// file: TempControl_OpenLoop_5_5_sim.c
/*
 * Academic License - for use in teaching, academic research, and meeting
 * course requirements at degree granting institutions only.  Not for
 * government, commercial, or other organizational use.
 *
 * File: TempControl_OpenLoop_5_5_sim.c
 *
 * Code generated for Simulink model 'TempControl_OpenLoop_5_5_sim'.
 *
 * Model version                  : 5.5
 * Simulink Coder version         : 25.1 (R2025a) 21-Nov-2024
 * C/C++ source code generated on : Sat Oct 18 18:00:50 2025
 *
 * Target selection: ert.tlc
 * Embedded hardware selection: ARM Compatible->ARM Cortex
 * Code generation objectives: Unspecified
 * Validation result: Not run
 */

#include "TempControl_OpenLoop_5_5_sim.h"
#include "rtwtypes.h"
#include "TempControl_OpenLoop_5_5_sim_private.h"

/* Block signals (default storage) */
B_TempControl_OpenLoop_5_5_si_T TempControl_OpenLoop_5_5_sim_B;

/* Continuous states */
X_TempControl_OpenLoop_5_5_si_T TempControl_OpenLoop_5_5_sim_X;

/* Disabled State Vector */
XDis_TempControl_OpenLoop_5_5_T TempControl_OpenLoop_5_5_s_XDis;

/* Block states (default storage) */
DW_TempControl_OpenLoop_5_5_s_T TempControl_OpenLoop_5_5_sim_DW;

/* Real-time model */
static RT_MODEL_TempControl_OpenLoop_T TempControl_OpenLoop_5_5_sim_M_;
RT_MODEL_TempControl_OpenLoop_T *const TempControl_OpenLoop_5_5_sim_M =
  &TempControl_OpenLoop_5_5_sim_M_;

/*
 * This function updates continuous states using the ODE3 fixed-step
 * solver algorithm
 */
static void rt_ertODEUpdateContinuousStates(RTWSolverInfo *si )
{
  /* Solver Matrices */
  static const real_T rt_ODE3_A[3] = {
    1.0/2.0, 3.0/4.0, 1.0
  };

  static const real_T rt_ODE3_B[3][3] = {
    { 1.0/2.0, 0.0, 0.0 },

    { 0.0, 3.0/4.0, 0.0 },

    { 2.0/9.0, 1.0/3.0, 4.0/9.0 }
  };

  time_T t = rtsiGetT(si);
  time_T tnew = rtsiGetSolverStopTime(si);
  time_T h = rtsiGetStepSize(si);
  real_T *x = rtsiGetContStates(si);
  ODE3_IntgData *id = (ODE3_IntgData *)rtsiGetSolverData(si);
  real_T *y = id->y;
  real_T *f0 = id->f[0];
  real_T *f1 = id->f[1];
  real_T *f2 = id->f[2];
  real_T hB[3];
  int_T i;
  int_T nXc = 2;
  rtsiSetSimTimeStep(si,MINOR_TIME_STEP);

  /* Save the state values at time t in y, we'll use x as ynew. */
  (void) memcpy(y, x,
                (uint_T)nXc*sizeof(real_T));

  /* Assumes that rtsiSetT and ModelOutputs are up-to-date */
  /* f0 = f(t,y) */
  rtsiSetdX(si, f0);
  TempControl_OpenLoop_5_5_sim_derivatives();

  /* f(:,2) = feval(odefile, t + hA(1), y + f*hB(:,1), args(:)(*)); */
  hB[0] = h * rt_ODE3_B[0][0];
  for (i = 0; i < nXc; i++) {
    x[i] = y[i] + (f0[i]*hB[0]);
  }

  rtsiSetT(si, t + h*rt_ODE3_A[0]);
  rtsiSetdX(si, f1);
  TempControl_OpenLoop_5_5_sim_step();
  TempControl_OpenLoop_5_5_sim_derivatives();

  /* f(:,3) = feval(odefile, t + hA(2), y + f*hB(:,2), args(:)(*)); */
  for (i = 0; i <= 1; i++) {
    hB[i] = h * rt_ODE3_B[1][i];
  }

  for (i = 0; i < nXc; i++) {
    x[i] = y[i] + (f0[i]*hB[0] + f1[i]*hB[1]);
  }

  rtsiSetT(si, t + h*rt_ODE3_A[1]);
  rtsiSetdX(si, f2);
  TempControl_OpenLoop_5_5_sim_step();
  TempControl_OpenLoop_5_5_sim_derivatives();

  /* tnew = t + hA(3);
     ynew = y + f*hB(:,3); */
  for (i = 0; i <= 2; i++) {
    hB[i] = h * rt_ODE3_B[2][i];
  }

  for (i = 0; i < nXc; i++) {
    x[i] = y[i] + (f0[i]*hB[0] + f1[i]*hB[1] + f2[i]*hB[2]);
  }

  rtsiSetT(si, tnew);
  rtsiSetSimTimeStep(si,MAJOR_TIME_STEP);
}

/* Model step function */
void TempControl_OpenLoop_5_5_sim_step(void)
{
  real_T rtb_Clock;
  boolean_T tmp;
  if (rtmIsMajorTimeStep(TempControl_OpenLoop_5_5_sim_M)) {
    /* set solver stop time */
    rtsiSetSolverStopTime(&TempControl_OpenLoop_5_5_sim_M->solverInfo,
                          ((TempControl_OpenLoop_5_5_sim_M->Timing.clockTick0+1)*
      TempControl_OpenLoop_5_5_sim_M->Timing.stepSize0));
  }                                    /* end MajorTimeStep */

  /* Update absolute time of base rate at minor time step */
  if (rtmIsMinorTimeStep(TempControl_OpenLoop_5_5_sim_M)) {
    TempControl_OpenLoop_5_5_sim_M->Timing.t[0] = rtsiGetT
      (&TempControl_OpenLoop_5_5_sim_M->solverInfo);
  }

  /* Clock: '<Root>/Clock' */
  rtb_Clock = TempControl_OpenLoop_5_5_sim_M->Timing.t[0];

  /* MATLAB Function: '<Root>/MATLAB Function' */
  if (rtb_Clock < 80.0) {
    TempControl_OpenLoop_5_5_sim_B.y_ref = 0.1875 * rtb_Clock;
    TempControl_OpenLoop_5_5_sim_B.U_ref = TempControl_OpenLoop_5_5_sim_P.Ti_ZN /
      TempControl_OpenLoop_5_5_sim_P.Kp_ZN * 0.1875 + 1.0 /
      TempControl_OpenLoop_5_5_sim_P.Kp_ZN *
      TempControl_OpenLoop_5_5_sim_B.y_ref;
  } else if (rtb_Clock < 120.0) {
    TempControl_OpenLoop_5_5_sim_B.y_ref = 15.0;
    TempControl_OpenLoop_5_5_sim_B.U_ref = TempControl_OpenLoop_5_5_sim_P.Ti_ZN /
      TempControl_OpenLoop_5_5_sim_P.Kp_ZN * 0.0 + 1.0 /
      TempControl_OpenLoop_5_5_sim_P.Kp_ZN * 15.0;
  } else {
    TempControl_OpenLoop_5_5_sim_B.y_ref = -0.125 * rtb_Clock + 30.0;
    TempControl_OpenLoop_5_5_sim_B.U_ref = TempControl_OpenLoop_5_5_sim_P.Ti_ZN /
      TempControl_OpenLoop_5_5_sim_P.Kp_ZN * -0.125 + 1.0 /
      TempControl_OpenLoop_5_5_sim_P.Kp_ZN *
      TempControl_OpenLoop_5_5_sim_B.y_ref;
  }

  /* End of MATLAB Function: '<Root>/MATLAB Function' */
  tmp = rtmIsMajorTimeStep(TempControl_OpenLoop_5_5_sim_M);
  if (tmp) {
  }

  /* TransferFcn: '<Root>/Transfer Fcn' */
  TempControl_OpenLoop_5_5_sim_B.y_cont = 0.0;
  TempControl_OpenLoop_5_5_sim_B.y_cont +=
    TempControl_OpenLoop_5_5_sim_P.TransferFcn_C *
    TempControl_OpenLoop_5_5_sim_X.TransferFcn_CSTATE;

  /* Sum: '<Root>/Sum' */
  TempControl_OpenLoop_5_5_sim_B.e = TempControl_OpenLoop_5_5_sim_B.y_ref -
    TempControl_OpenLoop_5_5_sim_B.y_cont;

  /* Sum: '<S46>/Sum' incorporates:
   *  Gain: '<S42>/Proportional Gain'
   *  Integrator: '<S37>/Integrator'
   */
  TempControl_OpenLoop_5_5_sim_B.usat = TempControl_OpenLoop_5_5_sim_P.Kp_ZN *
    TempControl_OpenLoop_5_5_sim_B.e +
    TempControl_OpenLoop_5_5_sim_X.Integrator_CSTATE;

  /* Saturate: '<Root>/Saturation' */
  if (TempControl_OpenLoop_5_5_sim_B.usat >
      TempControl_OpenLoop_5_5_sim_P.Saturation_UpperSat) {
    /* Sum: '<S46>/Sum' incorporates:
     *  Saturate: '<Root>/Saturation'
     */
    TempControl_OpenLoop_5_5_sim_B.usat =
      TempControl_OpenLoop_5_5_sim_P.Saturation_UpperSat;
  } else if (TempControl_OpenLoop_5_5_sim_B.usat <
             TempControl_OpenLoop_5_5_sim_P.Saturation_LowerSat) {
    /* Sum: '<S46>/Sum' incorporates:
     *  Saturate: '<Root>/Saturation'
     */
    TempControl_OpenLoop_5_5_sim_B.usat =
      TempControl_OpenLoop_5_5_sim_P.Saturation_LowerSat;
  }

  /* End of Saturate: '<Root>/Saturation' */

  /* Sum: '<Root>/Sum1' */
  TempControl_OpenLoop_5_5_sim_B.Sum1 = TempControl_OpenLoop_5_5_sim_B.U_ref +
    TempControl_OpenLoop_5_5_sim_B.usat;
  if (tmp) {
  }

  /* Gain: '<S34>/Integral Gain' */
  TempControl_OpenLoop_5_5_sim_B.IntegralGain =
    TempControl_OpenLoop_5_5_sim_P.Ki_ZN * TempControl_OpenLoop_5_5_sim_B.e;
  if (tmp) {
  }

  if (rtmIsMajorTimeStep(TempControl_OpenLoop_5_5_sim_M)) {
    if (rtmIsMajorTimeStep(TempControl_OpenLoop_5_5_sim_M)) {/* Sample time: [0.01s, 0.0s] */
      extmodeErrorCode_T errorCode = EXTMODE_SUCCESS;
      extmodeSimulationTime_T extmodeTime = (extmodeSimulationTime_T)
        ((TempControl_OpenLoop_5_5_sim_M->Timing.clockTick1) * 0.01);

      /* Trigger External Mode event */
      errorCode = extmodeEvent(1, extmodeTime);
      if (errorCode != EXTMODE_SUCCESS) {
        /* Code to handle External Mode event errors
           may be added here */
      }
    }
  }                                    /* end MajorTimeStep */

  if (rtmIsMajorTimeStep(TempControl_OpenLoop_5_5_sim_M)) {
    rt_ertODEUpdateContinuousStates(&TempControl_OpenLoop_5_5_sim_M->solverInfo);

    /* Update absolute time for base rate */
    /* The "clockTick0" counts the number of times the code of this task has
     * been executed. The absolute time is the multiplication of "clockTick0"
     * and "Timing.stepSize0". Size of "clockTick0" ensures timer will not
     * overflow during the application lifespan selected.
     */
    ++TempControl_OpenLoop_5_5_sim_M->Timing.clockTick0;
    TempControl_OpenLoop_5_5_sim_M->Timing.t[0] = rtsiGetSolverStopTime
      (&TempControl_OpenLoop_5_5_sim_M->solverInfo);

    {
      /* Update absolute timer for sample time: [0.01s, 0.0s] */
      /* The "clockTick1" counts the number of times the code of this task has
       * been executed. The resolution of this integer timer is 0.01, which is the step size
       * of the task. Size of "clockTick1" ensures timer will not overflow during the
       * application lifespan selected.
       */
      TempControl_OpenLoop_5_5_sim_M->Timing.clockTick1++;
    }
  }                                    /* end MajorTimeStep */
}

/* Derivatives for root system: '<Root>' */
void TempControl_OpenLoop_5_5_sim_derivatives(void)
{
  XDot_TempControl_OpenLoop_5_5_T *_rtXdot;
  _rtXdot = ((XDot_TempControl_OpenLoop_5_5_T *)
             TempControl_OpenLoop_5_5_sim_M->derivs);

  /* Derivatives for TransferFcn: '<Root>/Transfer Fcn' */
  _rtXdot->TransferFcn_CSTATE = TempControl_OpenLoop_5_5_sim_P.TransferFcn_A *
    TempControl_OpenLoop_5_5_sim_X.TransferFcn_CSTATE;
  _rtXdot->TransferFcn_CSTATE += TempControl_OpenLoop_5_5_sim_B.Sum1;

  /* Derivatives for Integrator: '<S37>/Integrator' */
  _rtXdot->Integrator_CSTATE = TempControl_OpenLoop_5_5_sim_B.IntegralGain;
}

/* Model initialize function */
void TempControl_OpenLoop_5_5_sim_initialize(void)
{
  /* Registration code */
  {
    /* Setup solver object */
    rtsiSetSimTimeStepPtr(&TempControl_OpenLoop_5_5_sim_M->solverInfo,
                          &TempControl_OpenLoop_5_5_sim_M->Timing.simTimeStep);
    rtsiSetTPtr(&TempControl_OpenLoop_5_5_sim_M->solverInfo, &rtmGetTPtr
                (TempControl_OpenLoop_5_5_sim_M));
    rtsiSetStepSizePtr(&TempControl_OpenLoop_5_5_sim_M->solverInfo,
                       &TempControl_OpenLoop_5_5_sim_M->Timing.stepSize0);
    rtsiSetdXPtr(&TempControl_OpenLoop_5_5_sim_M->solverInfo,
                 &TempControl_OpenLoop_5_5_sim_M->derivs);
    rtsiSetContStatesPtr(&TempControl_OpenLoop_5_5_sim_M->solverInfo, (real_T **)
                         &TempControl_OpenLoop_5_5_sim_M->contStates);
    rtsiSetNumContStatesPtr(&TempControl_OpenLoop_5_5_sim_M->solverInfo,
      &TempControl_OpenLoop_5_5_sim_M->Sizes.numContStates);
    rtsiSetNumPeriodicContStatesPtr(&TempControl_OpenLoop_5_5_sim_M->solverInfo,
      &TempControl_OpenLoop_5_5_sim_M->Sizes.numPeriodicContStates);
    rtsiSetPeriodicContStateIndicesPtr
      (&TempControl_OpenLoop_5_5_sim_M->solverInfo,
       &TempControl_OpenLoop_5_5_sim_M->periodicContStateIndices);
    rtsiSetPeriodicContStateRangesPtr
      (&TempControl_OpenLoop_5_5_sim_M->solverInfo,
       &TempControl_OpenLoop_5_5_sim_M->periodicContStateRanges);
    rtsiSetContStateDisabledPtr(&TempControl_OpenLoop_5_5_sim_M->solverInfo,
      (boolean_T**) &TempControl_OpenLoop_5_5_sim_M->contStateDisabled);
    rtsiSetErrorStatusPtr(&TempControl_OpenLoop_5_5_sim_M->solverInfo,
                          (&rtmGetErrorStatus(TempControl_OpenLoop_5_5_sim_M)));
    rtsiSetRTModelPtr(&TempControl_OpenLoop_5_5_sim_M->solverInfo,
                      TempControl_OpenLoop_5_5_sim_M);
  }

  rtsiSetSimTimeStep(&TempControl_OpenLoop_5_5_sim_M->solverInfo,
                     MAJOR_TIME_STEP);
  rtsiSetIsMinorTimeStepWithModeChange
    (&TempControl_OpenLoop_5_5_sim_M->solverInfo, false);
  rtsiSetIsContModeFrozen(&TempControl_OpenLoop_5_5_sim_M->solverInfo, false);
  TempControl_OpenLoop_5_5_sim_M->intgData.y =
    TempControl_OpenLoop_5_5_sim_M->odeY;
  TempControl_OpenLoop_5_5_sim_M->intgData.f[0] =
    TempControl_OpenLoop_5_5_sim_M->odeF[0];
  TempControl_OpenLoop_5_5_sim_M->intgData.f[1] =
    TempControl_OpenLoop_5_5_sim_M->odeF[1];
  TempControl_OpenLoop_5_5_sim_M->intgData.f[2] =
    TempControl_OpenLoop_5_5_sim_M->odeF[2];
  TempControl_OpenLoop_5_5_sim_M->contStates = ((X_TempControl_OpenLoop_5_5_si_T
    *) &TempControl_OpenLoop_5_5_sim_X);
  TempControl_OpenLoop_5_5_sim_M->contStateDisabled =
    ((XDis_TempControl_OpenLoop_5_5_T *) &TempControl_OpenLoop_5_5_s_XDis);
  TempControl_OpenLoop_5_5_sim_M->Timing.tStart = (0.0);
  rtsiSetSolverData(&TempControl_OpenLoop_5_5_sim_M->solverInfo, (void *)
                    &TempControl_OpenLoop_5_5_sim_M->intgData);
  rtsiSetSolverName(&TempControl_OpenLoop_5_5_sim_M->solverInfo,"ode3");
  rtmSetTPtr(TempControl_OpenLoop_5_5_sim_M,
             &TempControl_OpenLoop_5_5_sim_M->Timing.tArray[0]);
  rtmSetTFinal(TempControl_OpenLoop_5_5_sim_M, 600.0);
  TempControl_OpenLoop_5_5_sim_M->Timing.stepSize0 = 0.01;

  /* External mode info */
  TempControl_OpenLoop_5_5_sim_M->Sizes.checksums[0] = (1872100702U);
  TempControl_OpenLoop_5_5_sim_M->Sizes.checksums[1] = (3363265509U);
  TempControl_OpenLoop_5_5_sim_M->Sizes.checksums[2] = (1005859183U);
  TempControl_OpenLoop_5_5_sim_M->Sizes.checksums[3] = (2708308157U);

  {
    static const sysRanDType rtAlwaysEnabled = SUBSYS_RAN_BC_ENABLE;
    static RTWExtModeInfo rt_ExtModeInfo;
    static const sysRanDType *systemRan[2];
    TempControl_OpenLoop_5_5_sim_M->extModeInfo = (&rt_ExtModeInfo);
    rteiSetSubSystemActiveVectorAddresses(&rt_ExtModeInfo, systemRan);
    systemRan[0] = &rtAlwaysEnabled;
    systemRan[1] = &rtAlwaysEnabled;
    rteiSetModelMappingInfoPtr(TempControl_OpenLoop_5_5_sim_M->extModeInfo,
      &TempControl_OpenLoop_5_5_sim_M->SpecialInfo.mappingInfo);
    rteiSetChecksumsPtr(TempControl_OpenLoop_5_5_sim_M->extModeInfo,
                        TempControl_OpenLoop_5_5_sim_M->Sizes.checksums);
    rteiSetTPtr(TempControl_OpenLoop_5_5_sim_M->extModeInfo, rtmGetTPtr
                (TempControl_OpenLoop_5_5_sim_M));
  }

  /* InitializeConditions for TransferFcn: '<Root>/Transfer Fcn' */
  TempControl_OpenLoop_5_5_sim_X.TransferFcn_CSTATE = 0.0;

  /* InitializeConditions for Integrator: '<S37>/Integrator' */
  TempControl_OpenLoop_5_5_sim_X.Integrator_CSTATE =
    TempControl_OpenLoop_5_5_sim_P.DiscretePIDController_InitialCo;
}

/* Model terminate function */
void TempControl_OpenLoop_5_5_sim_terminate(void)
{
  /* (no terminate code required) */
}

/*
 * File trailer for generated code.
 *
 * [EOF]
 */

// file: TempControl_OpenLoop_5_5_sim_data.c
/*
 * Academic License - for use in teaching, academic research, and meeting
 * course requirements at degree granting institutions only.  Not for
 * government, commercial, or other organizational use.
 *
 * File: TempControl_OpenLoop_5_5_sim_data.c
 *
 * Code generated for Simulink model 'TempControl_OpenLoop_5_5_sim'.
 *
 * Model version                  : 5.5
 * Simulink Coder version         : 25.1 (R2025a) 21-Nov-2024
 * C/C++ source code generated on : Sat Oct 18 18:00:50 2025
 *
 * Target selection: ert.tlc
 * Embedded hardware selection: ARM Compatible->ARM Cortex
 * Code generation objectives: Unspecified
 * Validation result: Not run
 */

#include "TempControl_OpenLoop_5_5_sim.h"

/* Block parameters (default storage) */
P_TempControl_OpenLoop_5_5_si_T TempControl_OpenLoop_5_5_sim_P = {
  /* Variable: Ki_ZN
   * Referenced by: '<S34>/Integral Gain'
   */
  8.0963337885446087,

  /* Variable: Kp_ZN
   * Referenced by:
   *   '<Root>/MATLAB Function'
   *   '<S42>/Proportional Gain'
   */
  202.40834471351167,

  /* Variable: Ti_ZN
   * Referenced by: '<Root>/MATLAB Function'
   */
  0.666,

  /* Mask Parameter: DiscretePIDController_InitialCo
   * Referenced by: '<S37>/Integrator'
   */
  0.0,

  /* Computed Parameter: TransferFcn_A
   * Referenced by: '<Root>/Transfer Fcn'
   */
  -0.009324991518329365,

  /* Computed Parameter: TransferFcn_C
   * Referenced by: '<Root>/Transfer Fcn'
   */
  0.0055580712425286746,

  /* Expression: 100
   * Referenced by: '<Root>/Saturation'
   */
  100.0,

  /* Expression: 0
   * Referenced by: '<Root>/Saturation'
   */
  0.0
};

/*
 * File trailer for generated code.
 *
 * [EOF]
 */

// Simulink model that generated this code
simulink model "TempControl_OpenLoop_5_5_sim"  (R2025a)
settings: Solver=FixedStepAuto  StartTime=0.0  StopTime=600  FixedStep=10e-3  RelTol=1e-3  EnableMultiTasking=on
undefined symbols (not defined in the file or in its folder): G_s, Ki_ZN, Kp_ZN, Ti_ZN
libraries: slpidlib x1

== system TempControl_OpenLoop_5_5_sim ==
  Clock : Clock
  Discrete PID Controller : slpidlib/PID Controller  Controller=PI  Form=Parallel  TimeDomain=Continuous-time  UseExternalTs=off  SampleTime=-1  IntegratorMethod=Forward Euler  FilterMethod=Forward Euler  ControllerParametersSource=internal  P=Kp_ZN  I=Ki_ZN  UseKiTs=off  D=0  UseExternalDerivativeSource=off  N=100  UseFilter=on  TunerSelectOption=Transfer Function Based (PID Tuner App)  InitialConditionSource=internal  InitialConditionForIntegrator=0  InitialConditionForFilter=0  DifferentiatorICPrevScaledInput=0  ExternalReset=none  TrackingMode=off  Kt=1  LimitOutput=off  SatLimitsSource=internal  UpperSaturationLimit=inf  LowerSaturationLimit=-inf  LinearizeAsGain=off  AntiWindupMode=none  Kb=1  LimitIntegrator=off  UpperIntegratorSaturationLimit=inf  LowerIntegratorSaturationLimit=-inf  POutMin=[]  POutMax=[]  IOutMin=[]  IOutMax=[]  DOutMin=[]  DOutMax=[]  NOutMin=[]  NOutMax=[]  SumOutMin=[]  SumOutMax=[]  SaturationOutMin=[]  SaturationOutMax=[]  PParamMin=[]  PParamMax=[]  IParamMin=[]  IParamMax=[]  DParamMin=[]  DParamMax=[]  NParamMin=[]  NParamMax=[]  KbParamMin=[]  KbParamMax=[]  KtParamMin=[]  KtParamMax=[]  KbOutMin=[]  KbOutMax=[]  KtOutMin=[]  KtOutMax=[]  IntegratorOutMin=[]  IntegratorOutMax=[]  FilterOutMin=[]  FilterOutMax=[]  SumI1OutMin=[]  SumI1OutMax=[]  SumI2OutMin=[]  SumI2OutMax=[]  SumI3OutMin=[]  SumI3OutMax=[]  SumI4OutMin=[]  SumI4OutMax=[]  SumDOutMin=[]  SumDOutMax=[]  DifferentiatorOutMin=[]  DifferentiatorOutMax=[]  FilterDiffOutCoefMin=[]  FilterDiffOutCoefMax=[]  ReciprocalOutMin=[]  ReciprocalOutMax=[]  SumDenOutMin=[]  SumDenOutMax=[]  SumNumOutMin=[]  SumNumOutMax=[]  DivideOutMin=[]  DivideOutMax=[]  UdiffTsProdOutMin=[]  UdiffTsProdOutMax=[]  NTsProdOutMin=[]  NTsProdOutMax=[]  UintegralTsProdOutMin=[]  UintegralTsProdOutMax=[]  UngainTsProdOutMin=[]  UngainTsProdOutMax=[]  ClampingZeroOutDataTypeStr=Inherit: Inherit via back propagation  ClampingZeroOutMin=[]  ClampingZeroOutMax=[]  FilterDenConstantOutDataTypeStr=Inherit: Inherit via back propagation  FilterDenConstantOutMin=[]  FilterDenConstantOutMax=[]  PCopyOutDataTypeStr=Inherit: Inherit via back propagation  PCopyOutMin=[]  PCopyOutMax=[]  NCopyOutDataTypeStr=Inherit: Inherit via back propagation  NCopyOutMin=[]  NCopyOutMax=[]  IntegratorContinuousStateAttributes=''  IntegratorStateMustResolveToSignalObject=off  IntegratorRTWStateStorageClass=Auto  FilterContinuousStateAttributes=''  FilterStateMustResolveToSignalObject=off  FilterRTWStateStorageClass=Auto  ParallelPVariant=InternalParameters  IdealPVariant=Disabled  IVariant=InternalParameters  DVariant=Disabled  IntegratorVariant=Continuous  SatVariant=Disabled  AWVariant=Passthrough  PCopyVariant=Disabled  TRVariant=Disabled  FdbkBlocksVariant=Forward  IdealPFdbkVariant=Disabled  SatFdbkVariant=Disabled  DerivativeFilterVariant=Disabled  NVariant=Disabled  NCopyVariant=Disabled_SignalSpec  FilterICVariant=Disabled  IntegratorICVariant=InternalICs  ExternalResetVariant=Disabled  TRSumVariant=Passthrough  SumFdbkVariant=Disabled  SumVariant=Sum_PI  TsampFilterVariant=InternalTs  TsampNgainVariant=Passthrough  TsampIntegralVariant=Disabled_SignalSpec  ExternalSaturationOutDataTypeStr=Inherit: Same as second input  DerivativeSourceVariant=Disabled  PreIntVariant=InternalPreInt
  MATLAB Function : MATLAB Function  TreatAsAtomicUnit=on
  Saturation : Saturate  UpperLimit=100  LowerLimit=0
  Sum : Sum  Inputs=|+-
  Sum1 : Sum
  Transfer Fcn : TransferFcn  Numerator=G_s.num{1}  Denominator=G_s.den{1}
  Scope1 : Scope
  wires:
  Sum/1 -> Discrete PID Controller/1  "e"
  Discrete PID Controller/1 -> Saturation/1  "u"
  MATLAB Function/2(y_ref) -> Sum/1  "yref"
  Saturation/1 -> Sum1/2  "usat"
  Sum1/1 -> Transfer Fcn/1
  Clock/1 -> MATLAB Function/1(t)
  MATLAB Function/1(U_ref) -> Sum1/1  "uref"
  Transfer Fcn/1 -> Sum/2  "y"

== matlab function TempControl_OpenLoop_5_5_sim/MATLAB Function ==
function [U_ref, y_ref] = fcn(t,Ti_ZN,Kp_ZN)

if t<80 
    y_ref=15/80*t;
    U_ref = (Ti_ZN/Kp_ZN)*(15/80)+1/Kp_ZN*y_ref;
elseif t<120
    y_ref=0*t+15;
    U_ref = (Ti_ZN/Kp_ZN)*(0)+1/Kp_ZN*y_ref;
else
    y_ref=-15/120*t+30;
    U_ref = (Ti_ZN/Kp_ZN)*(-15/120)+1/Kp_ZN*y_ref;
end
